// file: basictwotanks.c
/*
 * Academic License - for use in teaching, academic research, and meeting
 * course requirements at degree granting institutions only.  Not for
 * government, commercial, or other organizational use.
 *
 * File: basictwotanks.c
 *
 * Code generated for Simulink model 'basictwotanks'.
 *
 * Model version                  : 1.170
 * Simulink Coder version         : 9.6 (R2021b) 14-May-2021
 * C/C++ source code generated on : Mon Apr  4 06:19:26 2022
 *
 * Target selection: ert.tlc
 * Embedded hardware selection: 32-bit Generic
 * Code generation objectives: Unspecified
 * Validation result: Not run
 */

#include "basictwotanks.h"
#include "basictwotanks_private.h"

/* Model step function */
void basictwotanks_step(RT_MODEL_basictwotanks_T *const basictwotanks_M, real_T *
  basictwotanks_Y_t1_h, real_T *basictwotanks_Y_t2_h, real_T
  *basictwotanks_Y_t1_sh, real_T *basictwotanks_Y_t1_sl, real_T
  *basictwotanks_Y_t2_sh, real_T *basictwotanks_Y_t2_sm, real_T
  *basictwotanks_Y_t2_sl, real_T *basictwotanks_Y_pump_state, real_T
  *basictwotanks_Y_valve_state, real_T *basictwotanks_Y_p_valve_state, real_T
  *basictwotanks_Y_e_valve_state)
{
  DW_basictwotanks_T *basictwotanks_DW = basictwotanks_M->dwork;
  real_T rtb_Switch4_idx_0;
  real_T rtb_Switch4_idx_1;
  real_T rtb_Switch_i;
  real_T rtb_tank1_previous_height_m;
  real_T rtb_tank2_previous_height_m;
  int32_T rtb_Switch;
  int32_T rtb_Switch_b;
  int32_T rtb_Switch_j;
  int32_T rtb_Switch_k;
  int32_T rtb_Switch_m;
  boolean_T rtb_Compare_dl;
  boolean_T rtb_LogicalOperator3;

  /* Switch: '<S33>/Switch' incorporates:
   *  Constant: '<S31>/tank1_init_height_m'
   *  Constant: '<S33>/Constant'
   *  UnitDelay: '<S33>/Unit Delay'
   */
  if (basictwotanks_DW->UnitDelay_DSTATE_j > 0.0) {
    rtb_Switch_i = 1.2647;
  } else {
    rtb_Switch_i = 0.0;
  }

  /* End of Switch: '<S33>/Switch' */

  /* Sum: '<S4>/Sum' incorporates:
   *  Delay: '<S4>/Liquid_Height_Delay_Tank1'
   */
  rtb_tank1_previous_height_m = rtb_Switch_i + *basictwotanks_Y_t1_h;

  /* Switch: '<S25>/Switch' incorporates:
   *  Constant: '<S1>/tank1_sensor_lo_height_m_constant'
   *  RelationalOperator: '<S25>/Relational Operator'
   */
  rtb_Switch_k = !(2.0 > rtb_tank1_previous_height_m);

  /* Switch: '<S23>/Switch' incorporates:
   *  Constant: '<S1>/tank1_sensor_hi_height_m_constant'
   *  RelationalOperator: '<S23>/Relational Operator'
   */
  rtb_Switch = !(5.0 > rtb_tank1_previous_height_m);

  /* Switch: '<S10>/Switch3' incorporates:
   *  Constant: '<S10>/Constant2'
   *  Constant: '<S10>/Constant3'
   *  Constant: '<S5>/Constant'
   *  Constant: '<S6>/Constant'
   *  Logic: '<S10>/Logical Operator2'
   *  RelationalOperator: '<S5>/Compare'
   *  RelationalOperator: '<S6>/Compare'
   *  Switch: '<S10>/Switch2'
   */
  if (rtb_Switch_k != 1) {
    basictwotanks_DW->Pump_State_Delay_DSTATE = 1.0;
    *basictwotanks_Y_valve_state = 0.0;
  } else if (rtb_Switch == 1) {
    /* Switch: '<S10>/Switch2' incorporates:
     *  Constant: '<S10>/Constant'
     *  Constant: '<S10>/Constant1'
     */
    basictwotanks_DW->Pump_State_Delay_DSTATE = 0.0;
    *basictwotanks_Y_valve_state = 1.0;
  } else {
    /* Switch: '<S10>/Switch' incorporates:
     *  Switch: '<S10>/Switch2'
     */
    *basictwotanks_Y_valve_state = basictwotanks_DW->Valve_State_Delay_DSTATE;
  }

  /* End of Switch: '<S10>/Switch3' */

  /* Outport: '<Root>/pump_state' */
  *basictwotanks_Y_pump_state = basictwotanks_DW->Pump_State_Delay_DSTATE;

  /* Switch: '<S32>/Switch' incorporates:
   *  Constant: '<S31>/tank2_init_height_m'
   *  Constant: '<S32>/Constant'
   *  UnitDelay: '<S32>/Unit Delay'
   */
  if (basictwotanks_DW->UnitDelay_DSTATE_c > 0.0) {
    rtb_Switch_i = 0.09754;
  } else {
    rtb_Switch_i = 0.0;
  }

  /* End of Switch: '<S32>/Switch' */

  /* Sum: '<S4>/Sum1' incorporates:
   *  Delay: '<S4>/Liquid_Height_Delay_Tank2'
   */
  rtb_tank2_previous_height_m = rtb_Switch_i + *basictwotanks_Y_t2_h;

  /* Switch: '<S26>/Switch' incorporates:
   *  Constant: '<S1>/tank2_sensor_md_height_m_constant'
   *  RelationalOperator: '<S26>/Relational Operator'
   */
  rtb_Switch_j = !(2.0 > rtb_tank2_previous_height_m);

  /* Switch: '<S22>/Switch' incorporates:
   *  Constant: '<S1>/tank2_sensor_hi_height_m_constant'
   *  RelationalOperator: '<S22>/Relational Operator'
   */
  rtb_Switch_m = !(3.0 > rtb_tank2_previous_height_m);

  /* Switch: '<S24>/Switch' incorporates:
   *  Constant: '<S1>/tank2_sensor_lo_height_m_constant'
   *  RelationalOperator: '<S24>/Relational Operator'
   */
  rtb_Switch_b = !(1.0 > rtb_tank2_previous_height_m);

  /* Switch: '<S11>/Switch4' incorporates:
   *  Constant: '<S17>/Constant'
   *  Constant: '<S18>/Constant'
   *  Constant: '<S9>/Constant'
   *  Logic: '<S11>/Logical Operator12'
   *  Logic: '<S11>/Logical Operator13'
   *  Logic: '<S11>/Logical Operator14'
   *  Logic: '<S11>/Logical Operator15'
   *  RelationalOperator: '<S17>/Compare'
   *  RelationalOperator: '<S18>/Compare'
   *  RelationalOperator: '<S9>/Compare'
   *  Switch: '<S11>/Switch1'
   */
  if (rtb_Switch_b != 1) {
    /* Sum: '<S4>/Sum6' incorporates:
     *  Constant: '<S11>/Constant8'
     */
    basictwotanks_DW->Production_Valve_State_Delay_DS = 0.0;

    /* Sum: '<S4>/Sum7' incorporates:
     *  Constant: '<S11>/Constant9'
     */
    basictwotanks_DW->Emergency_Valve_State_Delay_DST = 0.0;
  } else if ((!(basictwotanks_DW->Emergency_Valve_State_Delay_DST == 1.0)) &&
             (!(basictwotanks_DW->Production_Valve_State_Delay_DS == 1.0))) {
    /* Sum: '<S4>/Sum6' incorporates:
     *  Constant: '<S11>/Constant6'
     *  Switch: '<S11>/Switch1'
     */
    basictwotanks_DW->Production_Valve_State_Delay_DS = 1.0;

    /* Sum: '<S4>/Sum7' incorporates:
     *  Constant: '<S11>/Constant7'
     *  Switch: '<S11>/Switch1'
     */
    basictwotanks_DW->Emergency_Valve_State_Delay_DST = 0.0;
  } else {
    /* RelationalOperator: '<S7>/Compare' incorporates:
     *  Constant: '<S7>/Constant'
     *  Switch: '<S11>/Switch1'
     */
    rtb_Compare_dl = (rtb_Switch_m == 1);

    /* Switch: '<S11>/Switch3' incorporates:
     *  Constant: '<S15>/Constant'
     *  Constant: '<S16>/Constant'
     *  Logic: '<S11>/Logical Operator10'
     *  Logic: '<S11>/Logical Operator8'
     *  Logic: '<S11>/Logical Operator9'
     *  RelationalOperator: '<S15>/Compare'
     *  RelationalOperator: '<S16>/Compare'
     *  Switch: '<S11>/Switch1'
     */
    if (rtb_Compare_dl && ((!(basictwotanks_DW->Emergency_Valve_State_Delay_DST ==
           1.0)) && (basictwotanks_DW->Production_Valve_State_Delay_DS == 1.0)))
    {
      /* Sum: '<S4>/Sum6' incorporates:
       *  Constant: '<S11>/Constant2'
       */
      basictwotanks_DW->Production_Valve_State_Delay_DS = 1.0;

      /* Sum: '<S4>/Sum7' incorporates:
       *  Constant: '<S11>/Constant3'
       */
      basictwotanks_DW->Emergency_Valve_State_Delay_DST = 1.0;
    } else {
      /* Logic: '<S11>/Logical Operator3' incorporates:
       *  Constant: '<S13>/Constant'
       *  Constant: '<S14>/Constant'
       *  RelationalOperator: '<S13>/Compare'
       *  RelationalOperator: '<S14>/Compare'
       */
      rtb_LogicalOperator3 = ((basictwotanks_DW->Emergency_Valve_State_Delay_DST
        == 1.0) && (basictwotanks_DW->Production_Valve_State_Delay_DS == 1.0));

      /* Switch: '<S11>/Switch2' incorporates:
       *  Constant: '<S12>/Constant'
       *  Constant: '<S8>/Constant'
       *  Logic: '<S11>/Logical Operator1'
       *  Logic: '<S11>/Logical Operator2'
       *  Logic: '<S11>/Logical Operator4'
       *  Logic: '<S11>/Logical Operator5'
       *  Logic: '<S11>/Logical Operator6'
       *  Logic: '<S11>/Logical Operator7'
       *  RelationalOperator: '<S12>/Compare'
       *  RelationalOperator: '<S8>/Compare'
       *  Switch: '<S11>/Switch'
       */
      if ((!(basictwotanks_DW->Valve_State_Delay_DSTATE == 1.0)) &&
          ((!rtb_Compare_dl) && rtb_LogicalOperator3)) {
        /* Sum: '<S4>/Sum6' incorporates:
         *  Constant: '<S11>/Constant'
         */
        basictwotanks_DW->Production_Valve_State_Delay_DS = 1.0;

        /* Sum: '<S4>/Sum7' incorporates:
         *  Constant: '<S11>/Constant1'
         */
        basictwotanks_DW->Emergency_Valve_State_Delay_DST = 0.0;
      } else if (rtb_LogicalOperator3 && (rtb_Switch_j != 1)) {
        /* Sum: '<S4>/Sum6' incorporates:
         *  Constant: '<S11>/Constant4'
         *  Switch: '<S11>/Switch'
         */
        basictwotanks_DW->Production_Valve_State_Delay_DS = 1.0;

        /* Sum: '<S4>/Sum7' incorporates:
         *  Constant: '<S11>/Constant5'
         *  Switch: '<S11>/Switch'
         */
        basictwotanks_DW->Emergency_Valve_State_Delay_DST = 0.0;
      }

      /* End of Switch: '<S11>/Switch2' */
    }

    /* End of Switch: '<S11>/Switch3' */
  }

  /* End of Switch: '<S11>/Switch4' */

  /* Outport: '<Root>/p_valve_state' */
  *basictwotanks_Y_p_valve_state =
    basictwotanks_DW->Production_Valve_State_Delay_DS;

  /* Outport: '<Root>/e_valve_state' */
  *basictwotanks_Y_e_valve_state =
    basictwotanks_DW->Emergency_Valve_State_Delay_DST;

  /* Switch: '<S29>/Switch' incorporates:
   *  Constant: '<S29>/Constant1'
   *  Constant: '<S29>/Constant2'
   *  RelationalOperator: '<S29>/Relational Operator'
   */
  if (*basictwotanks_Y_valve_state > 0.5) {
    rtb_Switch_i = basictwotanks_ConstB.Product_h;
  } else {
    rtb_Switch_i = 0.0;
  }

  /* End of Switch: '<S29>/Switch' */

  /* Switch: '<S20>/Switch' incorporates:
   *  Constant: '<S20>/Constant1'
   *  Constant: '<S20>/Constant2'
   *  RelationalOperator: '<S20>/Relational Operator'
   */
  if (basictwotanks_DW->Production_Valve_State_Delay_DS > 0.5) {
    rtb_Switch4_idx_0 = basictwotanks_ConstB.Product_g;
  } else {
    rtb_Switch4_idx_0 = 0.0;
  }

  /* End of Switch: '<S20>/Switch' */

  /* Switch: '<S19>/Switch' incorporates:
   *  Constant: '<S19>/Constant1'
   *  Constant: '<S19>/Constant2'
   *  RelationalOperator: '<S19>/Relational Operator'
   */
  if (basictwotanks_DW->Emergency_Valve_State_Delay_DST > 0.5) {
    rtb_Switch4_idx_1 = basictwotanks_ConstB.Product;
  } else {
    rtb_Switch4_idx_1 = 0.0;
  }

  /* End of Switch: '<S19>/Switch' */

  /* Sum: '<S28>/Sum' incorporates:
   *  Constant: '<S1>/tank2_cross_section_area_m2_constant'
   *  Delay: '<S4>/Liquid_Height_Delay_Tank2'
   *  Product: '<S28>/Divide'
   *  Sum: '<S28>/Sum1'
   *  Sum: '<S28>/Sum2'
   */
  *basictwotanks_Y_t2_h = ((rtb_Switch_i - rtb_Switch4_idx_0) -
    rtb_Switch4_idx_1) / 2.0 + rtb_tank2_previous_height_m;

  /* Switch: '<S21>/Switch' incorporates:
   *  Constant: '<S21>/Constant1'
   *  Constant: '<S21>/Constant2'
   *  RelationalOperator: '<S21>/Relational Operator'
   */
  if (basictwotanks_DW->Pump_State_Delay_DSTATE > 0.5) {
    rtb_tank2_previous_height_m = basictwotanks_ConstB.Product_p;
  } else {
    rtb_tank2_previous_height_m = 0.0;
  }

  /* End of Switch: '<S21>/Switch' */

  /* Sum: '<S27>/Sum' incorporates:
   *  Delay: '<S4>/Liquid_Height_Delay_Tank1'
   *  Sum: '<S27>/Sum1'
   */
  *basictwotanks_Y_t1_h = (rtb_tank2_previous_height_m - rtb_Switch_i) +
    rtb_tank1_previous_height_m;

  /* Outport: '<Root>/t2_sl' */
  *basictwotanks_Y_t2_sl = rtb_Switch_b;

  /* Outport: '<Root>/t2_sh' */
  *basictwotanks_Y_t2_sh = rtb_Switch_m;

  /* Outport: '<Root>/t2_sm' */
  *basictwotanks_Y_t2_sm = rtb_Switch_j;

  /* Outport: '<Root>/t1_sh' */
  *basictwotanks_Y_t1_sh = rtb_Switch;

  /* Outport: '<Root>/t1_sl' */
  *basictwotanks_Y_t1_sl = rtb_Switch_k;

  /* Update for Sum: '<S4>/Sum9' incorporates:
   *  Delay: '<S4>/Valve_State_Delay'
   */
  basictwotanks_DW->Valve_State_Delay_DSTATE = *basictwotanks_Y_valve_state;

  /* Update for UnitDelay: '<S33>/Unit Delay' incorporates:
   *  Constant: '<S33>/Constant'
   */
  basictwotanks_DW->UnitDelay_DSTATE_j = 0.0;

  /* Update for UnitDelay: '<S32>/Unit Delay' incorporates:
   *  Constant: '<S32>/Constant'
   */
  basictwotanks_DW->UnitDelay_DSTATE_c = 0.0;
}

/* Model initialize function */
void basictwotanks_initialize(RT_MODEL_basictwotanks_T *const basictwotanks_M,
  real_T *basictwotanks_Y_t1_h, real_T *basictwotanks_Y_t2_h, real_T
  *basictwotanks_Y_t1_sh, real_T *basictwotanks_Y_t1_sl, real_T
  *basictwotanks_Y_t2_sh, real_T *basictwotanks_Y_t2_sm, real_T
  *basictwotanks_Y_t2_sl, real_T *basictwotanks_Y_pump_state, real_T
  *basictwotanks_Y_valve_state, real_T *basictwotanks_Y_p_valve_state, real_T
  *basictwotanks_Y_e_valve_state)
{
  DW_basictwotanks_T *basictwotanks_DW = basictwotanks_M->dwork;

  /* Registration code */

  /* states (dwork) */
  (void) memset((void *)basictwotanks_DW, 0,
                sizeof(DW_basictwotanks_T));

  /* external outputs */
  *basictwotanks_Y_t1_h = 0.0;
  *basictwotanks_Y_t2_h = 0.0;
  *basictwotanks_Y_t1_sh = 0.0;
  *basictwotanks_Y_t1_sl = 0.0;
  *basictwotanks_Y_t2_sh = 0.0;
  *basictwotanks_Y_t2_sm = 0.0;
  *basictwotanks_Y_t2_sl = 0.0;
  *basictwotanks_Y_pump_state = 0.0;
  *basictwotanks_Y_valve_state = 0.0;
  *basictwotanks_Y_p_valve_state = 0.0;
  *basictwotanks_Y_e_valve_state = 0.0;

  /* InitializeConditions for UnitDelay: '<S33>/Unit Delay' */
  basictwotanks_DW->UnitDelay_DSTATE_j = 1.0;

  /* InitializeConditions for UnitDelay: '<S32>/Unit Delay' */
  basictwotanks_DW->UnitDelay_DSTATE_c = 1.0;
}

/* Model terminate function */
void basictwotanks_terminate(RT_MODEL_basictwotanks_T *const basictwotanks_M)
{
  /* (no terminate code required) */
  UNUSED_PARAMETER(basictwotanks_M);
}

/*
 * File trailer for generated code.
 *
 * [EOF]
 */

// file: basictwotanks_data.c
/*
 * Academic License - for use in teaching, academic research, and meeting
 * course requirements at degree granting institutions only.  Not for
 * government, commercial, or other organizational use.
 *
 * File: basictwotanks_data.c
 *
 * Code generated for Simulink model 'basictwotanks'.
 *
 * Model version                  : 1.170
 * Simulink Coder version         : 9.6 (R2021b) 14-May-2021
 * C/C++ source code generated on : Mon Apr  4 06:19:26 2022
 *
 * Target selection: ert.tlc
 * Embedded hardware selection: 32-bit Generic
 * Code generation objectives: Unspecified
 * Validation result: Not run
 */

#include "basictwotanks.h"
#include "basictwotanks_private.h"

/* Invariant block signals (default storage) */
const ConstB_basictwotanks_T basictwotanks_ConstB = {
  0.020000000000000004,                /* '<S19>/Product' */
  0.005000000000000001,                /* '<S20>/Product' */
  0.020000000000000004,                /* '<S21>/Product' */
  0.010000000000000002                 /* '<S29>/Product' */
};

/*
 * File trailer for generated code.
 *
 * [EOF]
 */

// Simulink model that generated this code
simulink model "basictwotanks"  (R2018a)
settings: Solver=FixedStepDiscrete  StartTime=0.0  StopTime=12500  FixedStep=0.1  RelTol=1e-3  EnableMultiTasking=on
model workspace (MAT data in the model file):
  F = [0 0]
  Global = [3707764736 2 1 1 1 1]
  InputSize = 5
  Operation = 'value'
  X = [1.91912110987  0.7189344389; 0.667300428728  0.319032887648; 0.539327875678  0.291550549769; 1.11428719774  0.782058235411; 0.458496889769  0.886118463221]
  handle : class17 (value not decoded)
  curPath = '/Users/ceren.gebizli/Desktop/Shiva/QRA-Search/QRA-Search/Problems/SimulinkTesting'
  handle : class17 (value not decoded)
  input = [1.91912110987  0.7189344389; 0.667300428728  0.319032887648; 0.539327875678  0.291550549769; 1.11428719774  0.782058235411; 0.458496889769  0.886118463221]
  inputSize = 1
  j = 2
  handle : class17 (value not decoded)
  modelpath = '/Users/ceren.gebizli/Desktop/Shiva/QRA-Search/QRA-Search/SimulinkModels/10_twotank/'
  nbrInputs = 2
  nbrTimeSteps = 5001
  tank1_init_height_m = 1.91912110987
  tank2_init_height_m = 0.7189344389
  timestep = 2
  var : struct (value not decoded)
libraries: simulink x12

== system basictwotanks ==
  Bus Creator : BusCreator  Inputs=4
  Bus Creator2 : BusCreator  Inputs='tank1_liquid_height_m','tank2_liquid_height_m'
  Bus Creator4 : BusCreator  Inputs='tank1_SH_value','tank1_SL_value','tank2_SH_value','tank2_SM_value','tank2_SL_value'
  Bus Creator5 : BusCreator  Inputs='tank1_sensor_hi_height_m','tank1_sensor_lo_height_m','tank1_pump_flow_rate_m3s','tank1_valve_flow_rate_m3s','tank1_cross_section_area_m2','tank2_sensor_hi_height_m','tank2_sensor_md_height_m','tank2_sensor_lo_height_m','tank2_p_valve_flow_rate_m3s','tank2_e_valve_flow_rate_m3s','tank2_cross_section_area_m2'
  Bus Selector : BusSelector  OutputSignals=Pump_State,Valve_State,Production_Valve_State,Emergency_Valve_State
  Bus Selector2 : BusSelector  OutputSignals=tank1_previous_height_m,tank2_previous_height_m
  Bus Selector4 : BusSelector  OutputSignals=tank1_SH_value,tank1_SL_value,tank2_SH_value,tank2_SM_value,tank2_SL_value
  Bus Selector5 : BusSelector  OutputSignals=pre_Pump_State,pre_Valve_State,pre_P_Valve_State,pre_E_Valve_State
  Bus Selector6 : BusSelector  OutputSignals=tank1_sensor_hi_height_m,tank1_sensor_lo_height_m,tank1_pump_flow_rate_m3s,tank1_valve_flow_rate_m3s,tank1_cross_section_area_m2,tank2_sensor_hi_height_m,tank2_sensor_md_height_m,tank2_sensor_lo_height_m,tank2_p_valve_flow_rate_m3s,tank2_e_valve_flow_rate_m3s,tank2_cross_section_area_m2
  Constants : Subsystem
  Controller : Subsystem
  Emergency : Scope
  Environment : Subsystem
  Initializer_and_Updater : Subsystem
  Liquid Height : Scope
  "Pre emergency " : Scope
  Scope : Scope  NumInputPorts=5
  To Workspace : ToWorkspace  VariableName=simout  SaveFormat=Timeseries  SampleTime=-1
  time_increment_s : Constant  Value=0.1
  t1_h : Outport
  t2_h : Outport  Port=2
  t1_sh : Outport  Port=3
  t1_sl : Outport  Port=4
  t2_sh : Outport  Port=5
  t2_sm : Outport  Port=6
  t2_sl : Outport  Port=7
  pump_state : Outport  Port=8
  valve_state : Outport  Port=9
  p_valve_state : Outport  Port=10
  e_valve_state : Outport  Port=11
  wires:
  Constants/1(tank1_sensor_hi_height_m) -> Bus Creator5/1  "tank1_sensor_hi_height_m"
  Constants/2(tank1_sensor_lo_height_m) -> Bus Creator5/2  "tank1_sensor_lo_height_m"
  Constants/3(tank1_pump_flow_rate_m3s) -> Bus Creator5/3  "tank1_pump_flow_rate_m3s"
  Constants/4(tank1_valve_flow_rate_m3s) -> Bus Creator5/4  "tank1_valve_flow_rate_m3s"
  Constants/5(tank1_cross_section_area_m2) -> Bus Creator5/5  "tank1_cross_section_area_m2"
  Constants/6(tank2_sensor_hi_height_m) -> Bus Creator5/6  "tank2_sensor_hi_height_m"
  Constants/7(tank2_sensor_md_height_m) -> Bus Creator5/7  "tank2_sensor_md_height_m"
  Constants/8(tank2_sensor_lo_height_m) -> Bus Creator5/8  "tank2_sensor_lo_height_m"
  Constants/9(tank2_p_valve_flow_rate_m3s) -> Bus Creator5/9  "tank2_p_valve_flow_rate_m3s"
  Constants/10(tank2_e_valve_flow_rate_m3s) -> Bus Creator5/10  "tank2_e_valve_flow_rate_m3s"
  Constants/11(tank2_cross_section_area_m2) -> Bus Creator5/11  "tank2_cross_section_area_m2"
  Controller/4(Emergency_Valve_State) -> e_valve_state/1, Emergency/1, Scope/3, Bus Creator/4  "Emergency_Valve_State"
  Controller/3(Production_Valve_State) -> Scope/5, p_valve_state/1, Bus Creator/3  "Production_Valve_State"
  Controller/2(Valve_State) -> Bus Creator/2, valve_state/1  "Valve_State"
  Controller/1(Pump_State) -> pump_state/1, Bus Creator/1  "Pump_State"
  Bus Creator/1 -> Initializer_and_Updater/2(actuator_states), Bus Selector/1
  Bus Selector/1 -> Environment/14(Pump_State)  "<Pump_State>"
  Bus Selector/2 -> Environment/15(Valve_State)  "<Valve_State>"
  Bus Selector/3 -> Environment/16(Production_Valve_State)  "<Production_Valve_State>"
  Bus Selector/4 -> Environment/17(Emergency_Valve_State)  "<Emergency_Valve_State>"
  time_increment_s/1 -> Environment/18(time_increment)
  Environment/1(tank1_liquid_height_m) -> t1_h/1, Bus Creator2/1  "tank1_liquid_height_m"
  Environment/2(tank2_liquid_height_m) -> t2_h/1, Bus Creator2/2  "tank2_liquid_height_m"
  Bus Selector2/1 -> Environment/12(tank1_previous_height_m)  "<tank1_previous_height_m>"
  Bus Selector2/2 -> Environment/13(tank2_previous_height_m)  "<tank2_previous_height_m>"
  Bus Creator2/1 -> Initializer_and_Updater/1(liquid_height), Liquid Height/1, To Workspace/1
  Environment/3(tank1_SH_value) -> t1_sh/1, Bus Creator4/1  "tank1_SH_value"
  Environment/4(tank1_SL_value) -> t1_sl/1, Bus Creator4/2  "tank1_SL_value"
  Environment/5(tank2_SH_value) -> Scope/1, t2_sh/1, Bus Creator4/3  "tank2_SH_value"
  Environment/6(tank2_SM_value) -> Scope/2, t2_sm/1, Bus Creator4/4  "tank2_SM_value"
  Environment/7(tank2_SL_value) -> t2_sl/1, Bus Creator4/5  "tank2_SL_value"
  Bus Creator4/1 -> Bus Selector4/1
  Bus Selector5/4 -> "Pre emergency "/1, Scope/4, Controller/4(pre_E_Valve_State)  "<pre_E_Valve_State>"
  Bus Selector5/1 -> Controller/1(pre_Pump_State)  "<pre_Pump_State>"
  Bus Selector5/2 -> Controller/2(pre_Valve_State)  "<pre_Valve_State>"
  Bus Selector5/3 -> Controller/3(pre_P_Valve_State)  "<pre_P_Valve_State>"
  Bus Selector4/1 -> Controller/5(tank1_SH_value)  "<tank1_SH_value>"
  Bus Selector4/2 -> Controller/6(tank1_SL_value)  "<tank1_SL_value>"
  Bus Selector4/3 -> Controller/7(tank2_SH_value)  "<tank2_SH_value>"
  Bus Selector4/4 -> Controller/8(tank2_SM_value)  "<tank2_SM_value>"
  Bus Selector4/5 -> Controller/9(tank2_SL_value)  "<tank2_SL_value>"
  Bus Creator5/1 -> Bus Selector6/1
  Bus Selector6/1 -> Environment/1(tank1_sensor_hi_height_m)  "<tank1_sensor_hi_height_m>"
  Bus Selector6/2 -> Environment/2(tank1_sensor_lo_height_m)  "<tank1_sensor_lo_height_m>"
  Bus Selector6/3 -> Environment/3(tank1_pump_flow_rate_m3s)  "<tank1_pump_flow_rate_m3s>"
  Bus Selector6/4 -> Environment/4(tank1_valve_flow_rate_m3s)  "<tank1_valve_flow_rate_m3s>"
  Bus Selector6/5 -> Environment/5(tank1_cross_section_area_m2)  "<tank1_cross_section_area_m2>"
  Bus Selector6/6 -> Environment/6(tank2_sensor_hi_height_m)  "<tank2_sensor_hi_height_m>"
  Bus Selector6/7 -> Environment/7(tank2_sensor_md_height_m)  "<tank2_sensor_md_height_m>"
  Bus Selector6/8 -> Environment/8(tank2_sensor_lo_height_m)  "<tank2_sensor_lo_height_m>"
  Bus Selector6/9 -> Environment/9(tank2_p_valve_flow_rate_m3s)  "<tank2_p_valve_flow_rate_m3s>"
  Bus Selector6/10 -> Environment/10(tank2_e_valve_flow_rate_m3s)  "<tank2_e_valve_flow_rate_m3s>"
  Bus Selector6/11 -> Environment/11(tank2_cross_section_area_m2)  "<tank2_cross_section_area_m2>"
  Initializer_and_Updater/1(previous_heights) -> Bus Selector2/1
  Initializer_and_Updater/2(previous_actuator_states) -> Bus Selector5/1

== system basictwotanks/Constants ==
  tank1_cross_section_area_m2_constant : Constant  Value=1.0
  tank1_pump_flow_rate_m3s_constant : Constant  Value=0.2
  tank1_sensor_hi_height_m_constant : Constant  Value=5.0
  tank1_sensor_lo_height_m_constant : Constant  Value=2.0
  tank1_valve_flow_rate_m3s_constant : Constant  Value=0.1
  tank2_cross_section_area_m2_constant : Constant  Value=2.0
  tank2_e_valve_flow_rate_m3s_constant : Constant  Value=0.2
  tank2_p_valve_flow_rate_m3s_constant : Constant  Value=0.05
  tank2_sensor_hi_height_m_constant : Constant  Value=3.0
  tank2_sensor_lo_height_m_constant : Constant  Value=1.0
  tank2_sensor_md_height_m_constant : Constant  Value=2.0
  tank1_sensor_hi_height_m : Outport
  tank1_sensor_lo_height_m : Outport  Port=2
  tank1_pump_flow_rate_m3s : Outport  Port=3
  tank1_valve_flow_rate_m3s : Outport  Port=4
  tank1_cross_section_area_m2 : Outport  Port=5
  tank2_sensor_hi_height_m : Outport  Port=6
  tank2_sensor_md_height_m : Outport  Port=7
  tank2_sensor_lo_height_m : Outport  Port=8
  tank2_p_valve_flow_rate_m3s : Outport  Port=9
  tank2_e_valve_flow_rate_m3s : Outport  Port=10
  tank2_cross_section_area_m2 : Outport  Port=11
  wires:
  tank2_sensor_hi_height_m_constant/1 -> tank2_sensor_hi_height_m/1  "tank2_sensor_hi_height_m"
  tank2_sensor_lo_height_m_constant/1 -> tank2_sensor_lo_height_m/1  "tank2_sensor_low_height_m"
  tank1_sensor_hi_height_m_constant/1 -> tank1_sensor_hi_height_m/1  "tank1_sensor_hi_height_m"
  tank1_pump_flow_rate_m3s_constant/1 -> tank1_pump_flow_rate_m3s/1  "tank1_pump_flow_rate_m3s"
  tank1_cross_section_area_m2_constant/1 -> tank1_cross_section_area_m2/1  "tank1_cross_section_area_m2"
  tank1_valve_flow_rate_m3s_constant/1 -> tank1_valve_flow_rate_m3s/1  "tank1_valve_flow_rate_m3s"
  tank1_sensor_lo_height_m_constant/1 -> tank1_sensor_lo_height_m/1  "tank1_sensor_lo_height_m"
  tank2_p_valve_flow_rate_m3s_constant/1 -> tank2_p_valve_flow_rate_m3s/1  "tank2_p_valve_flow_rate_m3s"
  tank2_cross_section_area_m2_constant/1 -> tank2_cross_section_area_m2/1  "tank2_cross_section_area_m2"
  tank2_e_valve_flow_rate_m3s_constant/1 -> tank2_e_valve_flow_rate_m3s/1  "tank2_e_valve_flow_rate_m3s"
  tank2_sensor_md_height_m_constant/1 -> tank2_sensor_md_height_m/1  "tank2_sensor_md_height_m"

== system basictwotanks/Controller ==
  pre_Pump_State : Inport
  pre_Valve_State : Inport  Port=2
  pre_P_Valve_State : Inport  Port=3
  pre_E_Valve_State : Inport  Port=4
  tank1_SH_value : Inport  Port=5
  tank1_SL_value : Inport  Port=6
  tank2_SH_value : Inport  Port=7
  tank2_SM_value : Inport  Port=8
  tank2_SL_value : Inport  Port=9
  Compare To Constant{,1,4..6} (5 alike) : simulink/Logic and Bit Operations/Compare To Constant  relop===  const=1  OutDataTypeStr=boolean
  Emergency Valve State : Scope
  Production Valve State : Scope
  "Pump State " : Scope
  Tank1_Controller : Subsystem
  Tank2_Controller : Subsystem
  Valve State : Scope
  Pump_State : Outport
  Valve_State : Outport  Port=2
  Production_Valve_State : Outport  Port=3
  Emergency_Valve_State : Outport  Port=4
  wires:
  tank1_SL_value/1 -> Compare To Constant1/1
  tank2_SL_value/1 -> Compare To Constant6/1
  pre_E_Valve_State/1 -> Tank2_Controller/6(prev_E_Valve_State)
  Compare To Constant1/1 -> Tank1_Controller/2(SL_Input)
  Tank1_Controller/1(Pump_State) -> Pump_State/1, "Pump State "/1  "Pump_State"
  Tank1_Controller/2(Valve_State) -> Valve_State/1, Valve State/1  "Valve_State"
  Compare To Constant/1 -> Tank1_Controller/1(SH_Input)
  pre_Pump_State/1 -> Tank1_Controller/3(prev_Pump_State)
  tank2_SH_value/1 -> Compare To Constant4/1
  Compare To Constant6/1 -> Tank2_Controller/3(SL_Input)
  Compare To Constant4/1 -> Tank2_Controller/1(SH_Input)
  tank1_SH_value/1 -> Compare To Constant/1
  pre_Valve_State/1 -> Tank2_Controller/4(prev_Valve_State), Tank1_Controller/4(prev_Valve_State)
  Tank2_Controller/2(Emergency_Valve_State) -> Emergency_Valve_State/1, Emergency Valve State/1  "Emergency_Valve_State"
  tank2_SM_value/1 -> Compare To Constant5/1
  Compare To Constant5/1 -> Tank2_Controller/2(SM_Input)
  Tank2_Controller/1(Production_Valve_State) -> Production_Valve_State/1, Production Valve State/1  "Production_Valve_State"
  pre_P_Valve_State/1 -> Tank2_Controller/5(prev_P_Valve_State)

== system basictwotanks/Environment ==
  tank1_sensor_hi_height_m : Inport
  tank1_sensor_lo_height_m : Inport  Port=2
  tank1_pump_flow_rate_m3s : Inport  Port=3
  tank1_valve_flow_rate_m3s : Inport  Port=4
  tank1_cross_section_area_m2 : Inport  Port=5
  tank2_sensor_hi_height_m : Inport  Port=6
  tank2_sensor_md_height_m : Inport  Port=7
  tank2_sensor_lo_height_m : Inport  Port=8
  tank2_p_valve_flow_rate_m3s : Inport  Port=9
  tank2_e_valve_flow_rate_m3s : Inport  Port=10
  tank2_cross_section_area_m2 : Inport  Port=11
  tank1_previous_height_m : Inport  Port=12
  tank2_previous_height_m : Inport  Port=13
  Pump_State : Inport  Port=14
  Valve_State : Inport  Port=15
  Production_Valve_State : Inport  Port=16
  Emergency_Valve_State : Inport  Port=17
  time_increment : Inport  Port=18
  EmergencyValve : Subsystem
  ProductionValve : Subsystem
  Pump : Subsystem
  Sensor_HI_Tank2 : Subsystem
  Sensor_High_Tank1 : Subsystem
  Sensor_LO_Tank2 : Subsystem
  Sensor_Low_Tank1 : Subsystem
  Sensor_MD_Tank2 : Subsystem
  Tank1 : Subsystem
  Tank2 : Subsystem
  Valve : Subsystem
  tank1_liquid_height_m : Outport
  tank2_liquid_height_m : Outport  Port=2
  tank1_SH_value : Outport  Port=3
  tank1_SL_value : Outport  Port=4
  tank2_SH_value : Outport  Port=5
  tank2_SM_value : Outport  Port=6
  tank2_SL_value : Outport  Port=7
  wires:
  Tank1/1(liquid_height_m) -> tank1_liquid_height_m/1  "tank1_liquid_height_m"
  time_increment/1 -> Pump/3(time_increment1), Valve/3(time_increment1), EmergencyValve/3(time_increment1), ProductionValve/3(time_increment1)
  tank2_sensor_hi_height_m/1 -> Sensor_HI_Tank2/2(sensor_height)
  tank2_sensor_md_height_m/1 -> Sensor_MD_Tank2/2(sensor_height)
  Sensor_Low_Tank1/1(Sensor Value) -> tank1_SL_value/1  "tank1_SL_value"
  Sensor_HI_Tank2/1(Sensor Value) -> tank2_SH_value/1  "tank2_SH_value"
  Sensor_High_Tank1/1(Sensor Value) -> tank1_SH_value/1  "tank1_SH_value"
  tank1_pump_flow_rate_m3s/1 -> Pump/2(actuator_flow_rate_m3s)
  Sensor_LO_Tank2/1(Sensor Value) -> tank2_SL_value/1  "tank2_SL_value"
  tank2_sensor_lo_height_m/1 -> Sensor_LO_Tank2/2(sensor_height)
  tank1_valve_flow_rate_m3s/1 -> Valve/2(actuator_flow_rate_m3s)
  Sensor_MD_Tank2/1(Sensor Value) -> tank2_SM_value/1  "tank2_SM_value"
  tank2_p_valve_flow_rate_m3s/1 -> ProductionValve/2(actuator_flow_rate_m3s)
  tank2_previous_height_m/1 -> Sensor_HI_Tank2/1(current_height), Sensor_MD_Tank2/1(current_height), Tank2/5(previous_height_m), Sensor_LO_Tank2/1(current_height)
  EmergencyValve/1(flow_rate_m3dt) -> Tank2/3(e_valve_flow_m)  "tank2_e_valve_flow_m3dt"
  Pump/1(flow_rate_m3dt) -> Tank1/2(pump_flow_rate_m3dt)  "tank1_pump_flow_m3dt"
  Valve/1(flow_rate_m3dt) -> Tank2/1(valve_flow_m), Tank1/4(valve_flow_rate_m3dt)  "tank1_valve_flow_m3dt"
  ProductionValve/1(flow_rate_m3dt) -> Tank2/2(p_valve_flow_m)  "tank2_p_valve_flow_m3dt"
  tank2_e_valve_flow_rate_m3s/1 -> EmergencyValve/2(actuator_flow_rate_m3s)
  Valve_State/1 -> Valve/1(Actuator_State)
  Emergency_Valve_State/1 -> EmergencyValve/1(Actuator_State)
  Pump_State/1 -> Pump/1(Actuator_State)
  tank1_sensor_lo_height_m/1 -> Sensor_Low_Tank1/2(sensor_height)
  tank1_sensor_hi_height_m/1 -> Sensor_High_Tank1/2(sensor_height)
  Production_Valve_State/1 -> ProductionValve/1(Actuator_State)
  tank1_previous_height_m/1 -> Sensor_High_Tank1/1(current_height), Tank1/1(previous_height_m), Sensor_Low_Tank1/1(current_height)
  Tank2/1(liquid_height_m) -> tank2_liquid_height_m/1  "tank2_liquid_height_m"
  tank1_cross_section_area_m2/1 -> Tank1/3(cross_section_area_m2)
  tank2_cross_section_area_m2/1 -> Tank2/4(tank2_cross_sectional_area_m2)

== system basictwotanks/Initializer_and_Updater ==
  liquid_height : Inport
  actuator_states : Inport  Port=2
  Bus Creator1 : BusCreator  Inputs='pre_Pump_State','pre_Valve_State','pre_P_Valve_State','pre_E_Valve_State'
  Bus Creator3 : BusCreator  Inputs='tank1_previous_height_m','tank2_previous_height_m'
  Bus Selector1 : BusSelector  OutputSignals=Pump_State,Valve_State,Production_Valve_State,Emergency_Valve_State
  Bus Selector3 : BusSelector  OutputSignals=tank1_liquid_height_m,tank2_liquid_height_m
  E_Valve_Initial_State : Subsystem
  Emergency_Valve_State_Delay : Delay  DelayLength=1  InitialCondition=0
  Initial Conditions : Subsystem
  Initial_Height_Tank _2 : Subsystem
  Initial_Height_Tank_1 : Subsystem
  Liquid_Height_Delay_Tank1 : Delay  DelayLength=1  InitialCondition=0
  Liquid_Height_Delay_Tank2 : Delay  DelayLength=1  InitialCondition=0
  P_Valve_Initial_State : Subsystem
  Production_Valve_State_Delay : Delay  DelayLength=1  InitialCondition=0
  Pump_Initial_State : Subsystem
  Pump_State_Delay : Delay  DelayLength=1  InitialCondition=0
  "Scope for Tank1 Height " : Scope
  Scope for Tank2 Height : Scope
  Sum{,1,6..9} (6 alike) : Sum  Inputs=|++
  Valve_Initial_State : Subsystem
  Valve_State_Delay : Delay  DelayLength=1  InitialCondition=0
  previous_heights : Outport
  previous_actuator_states : Outport  Port=2
  wires:
  Production_Valve_State_Delay/1 -> Sum6/2
  Liquid_Height_Delay_Tank1/1 -> Sum/2
  Pump_Initial_State/1(Initial Value) -> Sum8/1
  Liquid_Height_Delay_Tank2/1 -> Sum1/2
  Valve_Initial_State/1(Initial Value) -> Sum9/1
  E_Valve_Initial_State/1(Initial Value) -> Sum7/1
  Emergency_Valve_State_Delay/1 -> Sum7/2
  Bus Selector1/3 -> Production_Valve_State_Delay/1  "<Production_Valve_State>"
  Bus Selector1/1 -> Pump_State_Delay/1  "<Pump_State>"
  Bus Selector1/2 -> Valve_State_Delay/1  "<Valve_State>"
  Bus Selector1/4 -> Emergency_Valve_State_Delay/1  "<Emergency_Valve_State>"
  Initial_Height_Tank_1/1(Initial Value) -> Sum/1
  Initial Conditions/3(tank1_pump_initial_state) -> Pump_Initial_State/1(initial_value)
  Initial Conditions/4(tank1_valve_initial_state) -> Valve_Initial_State/1(initial_value)
  Initial Conditions/1(tank1_initial_height_m) -> Initial_Height_Tank_1/1(initial_value)
  Initial Conditions/2(tank2_initial_height_m) -> Initial_Height_Tank _2/1(initial_value)
  Initial Conditions/5(tank2_p_valve_initial_state) -> P_Valve_Initial_State/1(initial_value)
  Initial Conditions/6(tank2_e_valve_initial_state) -> E_Valve_Initial_State/1(initial_value)
  P_Valve_Initial_State/1(Initial Value) -> Sum6/1
  Sum7/1 -> Bus Creator1/4  "pre_E_Valve_State"
  Bus Selector3/2 -> Scope for Tank2 Height/1, Liquid_Height_Delay_Tank2/1  "<tank2_liquid_height_m>"
  Bus Selector3/1 -> "Scope for Tank1 Height "/1, Liquid_Height_Delay_Tank1/1  "<tank1_liquid_height_m>"
  Bus Creator3/1 -> previous_heights/1
  Sum6/1 -> Bus Creator1/3  "pre_P_Valve_State"
  Sum/1 -> Bus Creator3/1  "tank1_previous_height_m"
  Sum9/1 -> Bus Creator1/2  "pre_Valve_State"
  Sum8/1 -> Bus Creator1/1  "pre_Pump_State"
  Sum1/1 -> Bus Creator3/2  "tank2_previous_height_m"
  Valve_State_Delay/1 -> Sum9/2
  Pump_State_Delay/1 -> Sum8/2
  Bus Creator1/1 -> previous_actuator_states/1
  liquid_height/1 -> Bus Selector3/1
  actuator_states/1 -> Bus Selector1/1
  Initial_Height_Tank _2/1(Initial Value) -> Sum1/1

== system basictwotanks/Controller/Tank1_Controller ==
  SH_Input : Inport
  SL_Input : Inport  Port=2
  prev_Pump_State : Inport  Port=3
  prev_Valve_State : Inport  Port=4
  Constant : Constant  Value=0.0
  Constant1 : Constant  Value=1.0
  Constant2 : Constant  Value=1.0
  Constant3 : Constant  Value=0.0
  Constant4 : Constant  Value=-1.0
  Constant5 : Constant  Value=-1.0
  Demux : Demux  Outputs=2
  Logical Operator : Logic  Operator=NOT  AllPortsSameDT=off  OutDataTypeStr=boolean
  Logical Operator1 : Logic  AllPortsSameDT=off  OutDataTypeStr=boolean
  Logical Operator2 : Logic  Operator=NOT  AllPortsSameDT=off  OutDataTypeStr=boolean
  Mux{,1..3} (4 alike) : Mux  Inputs=2
  Switch : Switch  Criteria=u2 ~= 0
  Switch2 : Switch  Criteria=u2 ~= 0
  Switch3 : Switch  Criteria=u2 ~= 0
  Pump_State : Outport
  Valve_State : Outport  Port=2
  wires:
  prev_Pump_State/1 -> [prev_Pump_State]
  prev_Valve_State/1 -> [prev_Valve_State]
  Mux/1 -> Switch/3
  Constant/1 -> Mux1/1
  Constant1/1 -> Mux1/2
  [prev_Pump_State] -> Mux2/1
  [prev_Valve_State] -> Mux2/2
  Mux2/1 -> Switch/1
  Logical Operator1/1 -> Switch/2
  [SL_Input] -> Logical Operator1/1
  Logical Operator/1 -> Logical Operator1/2
  [SH_Input] -> Logical Operator/1
  Switch/1 -> Switch2/3
  [SH_Input] -> Switch2/2
  Mux1/1 -> Switch2/1
  [SL_Input] -> Logical Operator2/1
  Constant2/1 -> Mux3/1
  Constant3/1 -> Mux3/2
  Mux3/1 -> Switch3/1
  Switch3/1 -> Demux/1
  Demux/2 -> Valve_State/1
  SH_Input/1 -> [SH_Input]
  SL_Input/1 -> [SL_Input]
  Logical Operator2/1 -> Switch3/2
  Constant4/1 -> Mux/1
  Constant5/1 -> Mux/2
  Demux/1 -> Pump_State/1
  Switch2/1 -> Switch3/3

== system basictwotanks/Controller/Tank2_Controller ==
  note: P: Open
      | E: Closed
  note: P: Open
      | E: Closed
  note: P: Open
      | E: Open
  note: P: Open
      | E: Closed
  note: P: Closed
      | E: Closed
  SH_Input : Inport
  SM_Input : Inport  Port=2
  SL_Input : Inport  Port=3
  prev_Valve_State : Inport  Port=4
  prev_P_Valve_State : Inport  Port=5
  prev_E_Valve_State : Inport  Port=6
  Compare To Constant{1..7} (7 alike) : simulink/Logic and Bit Operations/Compare To Constant  relop===  const=1  OutDataTypeStr=boolean
  Constant{,2..4,6} (5 alike) : Constant  Value=1.0
  Constant{1,5,7..9} (5 alike) : Constant  Value=0.0
  Demux : Demux  Outputs=2
  Logical Operator{1,3..4,6,8,10..12} (8 alike) : Logic  AllPortsSameDT=off  OutDataTypeStr=boolean
  Logical Operator{2,5,7,9,13..15} (7 alike) : Logic  Operator=NOT  AllPortsSameDT=off  OutDataTypeStr=boolean
  Mux{,1..5} (6 alike) : Mux  Inputs=2
  Switch{,1..4} (5 alike) : Switch  Criteria=u2 ~= 0
  Production_Valve_State : Outport
  Emergency_Valve_State : Outport  Port=2
  wires:
  SH_Input/1 -> [SH_Input]
  SL_Input/1 -> [SL_Input]
  SM_Input/1 -> [SM_Input]
  prev_E_Valve_State/1 -> [prev_E_Valve_State]
  prev_Valve_State/1 -> [prev_Valve_State]
  prev_P_Valve_State/1 -> [prev_P_Valve_State]
  [prev_P_Valve_State] -> Mux/1
  [prev_E_Valve_State] -> Mux/2
  Mux/1 -> Switch/3
  Constant/1 -> Mux1/1
  Constant1/1 -> Mux1/2
  Logical Operator1/1 -> Switch/2
  [SM_Input] -> Logical Operator2/1
  Switch/1 -> Switch2/3
  Logical Operator4/1 -> Switch2/2
  Mux1/1 -> Switch2/1
  Switch2/1 -> Switch3/3
  Logical Operator10/1 -> Switch3/2
  Demux/1 -> Production_Valve_State/1
  Demux/2 -> Emergency_Valve_State/1
  [prev_E_Valve_State] -> Compare To Constant2/1
  [prev_P_Valve_State] -> Compare To Constant3/1
  [prev_Valve_State] -> Compare To Constant1/1
  Logical Operator5/1 -> Logical Operator4/1
  Logical Operator6/1 -> Logical Operator4/2
  Logical Operator3/1 -> Logical Operator6/2, Logical Operator1/1
  Logical Operator2/1 -> Logical Operator1/2
  [SH_Input] -> Logical Operator7/1
  Logical Operator7/1 -> Logical Operator6/1
  Constant4/1 -> Mux2/1
  Constant5/1 -> Mux2/2
  Mux2/1 -> Switch/1
  [prev_E_Valve_State] -> Compare To Constant4/1
  [prev_P_Valve_State] -> Compare To Constant5/1
  Logical Operator9/1 -> Logical Operator8/1
  Logical Operator8/1 -> Logical Operator10/2
  Constant2/1 -> Mux3/1
  Constant3/1 -> Mux3/2
  Mux3/1 -> Switch3/1
  [prev_E_Valve_State] -> Compare To Constant6/1
  [prev_P_Valve_State] -> Compare To Constant7/1
  Logical Operator13/1 -> Logical Operator12/1
  Logical Operator12/1 -> Logical Operator11/2
  [SL_Input] -> Logical Operator11/1
  Logical Operator14/1 -> Logical Operator12/2
  Switch3/1 -> Switch1/3
  Logical Operator11/1 -> Switch1/2
  Constant6/1 -> Mux4/1
  Constant7/1 -> Mux4/2
  Mux4/1 -> Switch1/1
  Switch1/1 -> Switch4/3
  Logical Operator15/1 -> Switch4/2
  [SL_Input] -> Logical Operator15/1
  Switch4/1 -> Demux/1
  Constant8/1 -> Mux5/1
  Constant9/1 -> Mux5/2
  Mux5/1 -> Switch4/1
  [SH_Input] -> Logical Operator10/1
  Compare To Constant1/1 -> Logical Operator5/1
  Compare To Constant2/1 -> Logical Operator3/1
  Compare To Constant3/1 -> Logical Operator3/2
  Compare To Constant4/1 -> Logical Operator9/1
  Compare To Constant5/1 -> Logical Operator8/2
  Compare To Constant6/1 -> Logical Operator13/1
  Compare To Constant7/1 -> Logical Operator14/1

== system basictwotanks/Environment/EmergencyValve ==
  Actuator_State : Inport
  actuator_flow_rate_m3s : Inport  Port=2
  time_increment1 : Inport  Port=3
  Constant1 : Constant  Value=0.0
  Constant2 : Constant  Value=0.5
  Product : Product
  Relational Operator : RelationalOperator  Operator=>  OutDataTypeStr=boolean  RndMeth=Nearest
  Switch : Switch  Criteria=u2 ~= 0
  flow_rate_m3dt : Outport
  wires:
  Relational Operator/1 -> Switch/2
  [as] -> Relational Operator/1
  [ti] -> Product/2
  Constant1/1 -> Switch/3
  Constant2/1 -> Relational Operator/2
  Actuator_State/1 -> [as]
  actuator_flow_rate_m3s/1 -> [afr]
  Switch/1 -> flow_rate_m3dt/1
  Product/1 -> Switch/1
  time_increment1/1 -> [ti]
  [afr] -> Product/1

== system basictwotanks/Environment/ProductionValve ==
  Actuator_State : Inport
  actuator_flow_rate_m3s : Inport  Port=2
  time_increment1 : Inport  Port=3
  Constant1 : Constant  Value=0.0
  Constant2 : Constant  Value=0.5
  Product : Product
  Relational Operator : RelationalOperator  Operator=>  OutDataTypeStr=boolean  RndMeth=Nearest
  Switch : Switch  Criteria=u2 ~= 0
  flow_rate_m3dt : Outport
  wires:
  [afr] -> Product/1
  time_increment1/1 -> [ti]
  Product/1 -> Switch/1
  Switch/1 -> flow_rate_m3dt/1
  actuator_flow_rate_m3s/1 -> [afr]
  Actuator_State/1 -> [as]
  Constant2/1 -> Relational Operator/2
  Constant1/1 -> Switch/3
  [ti] -> Product/2
  [as] -> Relational Operator/1
  Relational Operator/1 -> Switch/2

== system basictwotanks/Environment/Pump ==
  Actuator_State : Inport
  actuator_flow_rate_m3s : Inport  Port=2
  time_increment1 : Inport  Port=3
  Constant1 : Constant  Value=0.0
  Constant2 : Constant  Value=0.5
  Product : Product
  Relational Operator : RelationalOperator  Operator=>  OutDataTypeStr=boolean  RndMeth=Nearest
  Switch : Switch  Criteria=u2 ~= 0
  flow_rate_m3dt : Outport
  wires:
  [afr] -> Product/1
  time_increment1/1 -> [ti]
  Product/1 -> Switch/1
  Switch/1 -> flow_rate_m3dt/1
  actuator_flow_rate_m3s/1 -> [afr]
  Actuator_State/1 -> [as]
  Constant2/1 -> Relational Operator/2
  Constant1/1 -> Switch/3
  [ti] -> Product/2
  [as] -> Relational Operator/1
  Relational Operator/1 -> Switch/2

== system basictwotanks/Environment/Sensor_HI_Tank2 ==
  current_height : Inport
  sensor_height : Inport  Port=2
  Constant : Constant  Value=0.0
  Constant1 : Constant  Value=1.0
  Relational Operator : RelationalOperator  Operator=>  OutDataTypeStr=boolean  RndMeth=Nearest
  Switch : Switch  Criteria=u2 ~= 0
  Sensor Value : Outport
  wires:
  Constant/1 -> Switch/1
  sensor_height/1 -> [sh]
  [sh] -> Relational Operator/1
  Constant1/1 -> Switch/3
  Relational Operator/1 -> Switch/2
  current_height/1 -> [ch]
  [ch] -> Relational Operator/2
  Switch/1 -> Sensor Value/1

== system basictwotanks/Environment/Sensor_High_Tank1 ==
  current_height : Inport
  sensor_height : Inport  Port=2
  Constant : Constant  Value=0.0
  Constant1 : Constant  Value=1.0
  Relational Operator : RelationalOperator  Operator=>  OutDataTypeStr=boolean  RndMeth=Nearest
  Switch : Switch  Criteria=u2 ~= 0
  Sensor Value : Outport
  wires:
  Constant/1 -> Switch/1
  sensor_height/1 -> [sh]
  [sh] -> Relational Operator/1
  Constant1/1 -> Switch/3
  Relational Operator/1 -> Switch/2
  current_height/1 -> [ch]
  [ch] -> Relational Operator/2
  Switch/1 -> Sensor Value/1

== system basictwotanks/Environment/Sensor_LO_Tank2 ==
  current_height : Inport
  sensor_height : Inport  Port=2
  Constant : Constant  Value=0.0
  Constant1 : Constant  Value=1.0
  Relational Operator : RelationalOperator  Operator=>  OutDataTypeStr=boolean  RndMeth=Nearest
  Switch : Switch  Criteria=u2 ~= 0
  Sensor Value : Outport
  wires:
  Constant/1 -> Switch/1
  sensor_height/1 -> [sh]
  [sh] -> Relational Operator/1
  Constant1/1 -> Switch/3
  Relational Operator/1 -> Switch/2
  current_height/1 -> [ch]
  [ch] -> Relational Operator/2
  Switch/1 -> Sensor Value/1

== system basictwotanks/Environment/Sensor_Low_Tank1 ==
  current_height : Inport
  sensor_height : Inport  Port=2
  Constant : Constant  Value=0.0
  Constant1 : Constant  Value=1.0
  Relational Operator : RelationalOperator  Operator=>  OutDataTypeStr=boolean  RndMeth=Nearest
  Switch : Switch  Criteria=u2 ~= 0
  Sensor Value : Outport
  wires:
  Switch/1 -> Sensor Value/1
  [ch] -> Relational Operator/2
  current_height/1 -> [ch]
  Relational Operator/1 -> Switch/2
  Constant1/1 -> Switch/3
  [sh] -> Relational Operator/1
  sensor_height/1 -> [sh]
  Constant/1 -> Switch/1

== system basictwotanks/Environment/Sensor_MD_Tank2 ==
  current_height : Inport
  sensor_height : Inport  Port=2
  Constant : Constant  Value=0.0
  Constant1 : Constant  Value=1.0
  Relational Operator : RelationalOperator  Operator=>  OutDataTypeStr=boolean  RndMeth=Nearest
  Switch : Switch  Criteria=u2 ~= 0
  Sensor Value : Outport
  wires:
  Switch/1 -> Sensor Value/1
  [ch] -> Relational Operator/2
  current_height/1 -> [ch]
  Relational Operator/1 -> Switch/2
  Constant1/1 -> Switch/3
  [sh] -> Relational Operator/1
  sensor_height/1 -> [sh]
  Constant/1 -> Switch/1

== system basictwotanks/Environment/Tank1 ==
  previous_height_m : Inport
  pump_flow_rate_m3dt : Inport  Port=2
  cross_section_area_m2 : Inport  Port=3
  valve_flow_rate_m3dt : Inport  Port=4
  Divide : Product  Inputs=*/
  Sum : Sum  Inputs=|++
  Sum1 : Sum  Inputs=|+-
  liquid_height_m : Outport
  wires:
  cross_section_area_m2/1 -> [csa]
  [ph] -> Sum/1
  Divide/1 -> Sum/2
  valve_flow_rate_m3dt/1 -> [vfr]
  [csa] -> Divide/2
  Sum1/1 -> Divide/1
  previous_height_m/1 -> [ph]
  [vfr] -> Sum1/2
  pump_flow_rate_m3dt/1 -> [pfr]
  [pfr] -> Sum1/1
  Sum/1 -> liquid_height_m/1

== system basictwotanks/Environment/Tank2 ==
  valve_flow_m : Inport
  p_valve_flow_m : Inport  Port=2
  e_valve_flow_m : Inport  Port=3
  tank2_cross_sectional_area_m2 : Inport  Port=4
  previous_height_m : Inport  Port=5
  Divide : Product  Inputs=*/
  Sum : Sum  Inputs=|++
  Sum1 : Sum  Inputs=|+-
  Sum2 : Sum  Inputs=|+-
  liquid_height_m : Outport
  wires:
  [evf] -> Sum2/2
  valve_flow_m/1 -> [vf]
  Sum/1 -> liquid_height_m/1
  p_valve_flow_m/1 -> [pvf]
  Divide/1 -> Sum/2
  [csa] -> Divide/2
  [ph] -> Sum/1
  tank2_cross_sectional_area_m2/1 -> [csa]
  previous_height_m/1 -> [ph]
  [vf] -> Sum1/1
  e_valve_flow_m/1 -> [evf]
  Sum2/1 -> Divide/1
  [pvf] -> Sum1/2
  Sum1/1 -> Sum2/1

== system basictwotanks/Environment/Valve ==
  Actuator_State : Inport
  actuator_flow_rate_m3s : Inport  Port=2
  time_increment1 : Inport  Port=3
  Constant1 : Constant  Value=0.0
  Constant2 : Constant  Value=0.5
  Product : Product
  Relational Operator : RelationalOperator  Operator=>  OutDataTypeStr=boolean  RndMeth=Nearest
  Switch : Switch  Criteria=u2 ~= 0
  flow_rate_m3dt : Outport
  wires:
  Relational Operator/1 -> Switch/2
  [as] -> Relational Operator/1
  [ti] -> Product/2
  Constant1/1 -> Switch/3
  Constant2/1 -> Relational Operator/2
  Actuator_State/1 -> [as]
  actuator_flow_rate_m3s/1 -> [afr]
  Switch/1 -> flow_rate_m3dt/1
  Product/1 -> Switch/1
  time_increment1/1 -> [ti]
  [afr] -> Product/1

== system basictwotanks/Initializer_and_Updater/E_Valve_Initial_State ==
  initial_value : Inport
  Constant : Constant  Value=0.0
  Switch : Switch  Criteria=u2 > Threshold
  Unit Delay : UnitDelay  InitialCondition=1  SampleTime=-1
  Initial Value : Outport
  wires:
  Switch/1 -> Initial Value/1
  Constant/1 -> Switch/3, Unit Delay/1
  Unit Delay/1 -> Switch/2
  initial_value/1 -> Switch/1

== system basictwotanks/Initializer_and_Updater/Initial Conditions ==
  tank1_init_height_m : Constant  Value=1.2647
  tank1_pump_init_state : Constant  Value=0.0
  tank1_valve_init_state : Constant  Value=0.0
  tank2_e_valve_init_state : Constant  Value=0.0
  tank2_init_height_m : Constant  Value=0.09754
  tank2_p_valve_init_state : Constant  Value=0.0
  tank1_initial_height_m : Outport
  tank2_initial_height_m : Outport  Port=2
  tank1_pump_initial_state : Outport  Port=3
  tank1_valve_initial_state : Outport  Port=4
  tank2_p_valve_initial_state : Outport  Port=5
  tank2_e_valve_initial_state : Outport  Port=6
  wires:
  tank1_pump_init_state/1 -> tank1_pump_initial_state/1  "tank1_pump_initial_state"
  tank2_e_valve_init_state/1 -> tank2_e_valve_initial_state/1  "tank2_e_valve_initial_state"
  tank2_p_valve_init_state/1 -> tank2_p_valve_initial_state/1  "tank2_p_valve_initial_state"
  tank1_init_height_m/1 -> tank1_initial_height_m/1  "tank1_initial_height_m"
  tank2_init_height_m/1 -> tank2_initial_height_m/1  "tank2_initial_height_m"
  tank1_valve_init_state/1 -> tank1_valve_initial_state/1  "tank1_valve_initial_state"

== system basictwotanks/Initializer_and_Updater/Initial_Height_Tank _2 ==
  initial_value : Inport
  Constant : Constant  Value=0.0
  Switch : Switch  Criteria=u2 > Threshold
  Unit Delay : UnitDelay  InitialCondition=1  SampleTime=-1
  Initial Value : Outport
  wires:
  Switch/1 -> Initial Value/1
  Constant/1 -> Switch/3, Unit Delay/1
  Unit Delay/1 -> Switch/2
  initial_value/1 -> Switch/1

== system basictwotanks/Initializer_and_Updater/Initial_Height_Tank_1 ==
  initial_value : Inport
  Constant : Constant  Value=0.0
  Switch : Switch  Criteria=u2 > Threshold
  Unit Delay : UnitDelay  InitialCondition=1  SampleTime=-1
  Initial Value : Outport
  wires:
  Constant/1 -> Switch/3, Unit Delay/1
  Unit Delay/1 -> Switch/2
  initial_value/1 -> Switch/1
  Switch/1 -> Initial Value/1

== system basictwotanks/Initializer_and_Updater/P_Valve_Initial_State ==
  initial_value : Inport
  Constant : Constant  Value=0.0
  Switch : Switch  Criteria=u2 > Threshold
  Unit Delay : UnitDelay  InitialCondition=1  SampleTime=-1
  Initial Value : Outport
  wires:
  Switch/1 -> Initial Value/1
  Constant/1 -> Switch/3, Unit Delay/1
  Unit Delay/1 -> Switch/2
  initial_value/1 -> Switch/1

== system basictwotanks/Initializer_and_Updater/Pump_Initial_State ==
  initial_value : Inport
  Constant : Constant  Value=0.0
  Switch : Switch  Criteria=u2 > Threshold
  Unit Delay : UnitDelay  InitialCondition=1  SampleTime=-1
  Initial Value : Outport
  wires:
  Switch/1 -> Initial Value/1
  Constant/1 -> Switch/3, Unit Delay/1
  Unit Delay/1 -> Switch/2
  initial_value/1 -> Switch/1

== system basictwotanks/Initializer_and_Updater/Valve_Initial_State ==
  initial_value : Inport
  Constant : Constant  Value=0.0
  Switch : Switch  Criteria=u2 > Threshold
  Unit Delay : UnitDelay  InitialCondition=1  SampleTime=-1
  Initial Value : Outport
  wires:
  Switch/1 -> Initial Value/1
  Constant/1 -> Switch/3, Unit Delay/1
  Unit Delay/1 -> Switch/2
  initial_value/1 -> Switch/1
